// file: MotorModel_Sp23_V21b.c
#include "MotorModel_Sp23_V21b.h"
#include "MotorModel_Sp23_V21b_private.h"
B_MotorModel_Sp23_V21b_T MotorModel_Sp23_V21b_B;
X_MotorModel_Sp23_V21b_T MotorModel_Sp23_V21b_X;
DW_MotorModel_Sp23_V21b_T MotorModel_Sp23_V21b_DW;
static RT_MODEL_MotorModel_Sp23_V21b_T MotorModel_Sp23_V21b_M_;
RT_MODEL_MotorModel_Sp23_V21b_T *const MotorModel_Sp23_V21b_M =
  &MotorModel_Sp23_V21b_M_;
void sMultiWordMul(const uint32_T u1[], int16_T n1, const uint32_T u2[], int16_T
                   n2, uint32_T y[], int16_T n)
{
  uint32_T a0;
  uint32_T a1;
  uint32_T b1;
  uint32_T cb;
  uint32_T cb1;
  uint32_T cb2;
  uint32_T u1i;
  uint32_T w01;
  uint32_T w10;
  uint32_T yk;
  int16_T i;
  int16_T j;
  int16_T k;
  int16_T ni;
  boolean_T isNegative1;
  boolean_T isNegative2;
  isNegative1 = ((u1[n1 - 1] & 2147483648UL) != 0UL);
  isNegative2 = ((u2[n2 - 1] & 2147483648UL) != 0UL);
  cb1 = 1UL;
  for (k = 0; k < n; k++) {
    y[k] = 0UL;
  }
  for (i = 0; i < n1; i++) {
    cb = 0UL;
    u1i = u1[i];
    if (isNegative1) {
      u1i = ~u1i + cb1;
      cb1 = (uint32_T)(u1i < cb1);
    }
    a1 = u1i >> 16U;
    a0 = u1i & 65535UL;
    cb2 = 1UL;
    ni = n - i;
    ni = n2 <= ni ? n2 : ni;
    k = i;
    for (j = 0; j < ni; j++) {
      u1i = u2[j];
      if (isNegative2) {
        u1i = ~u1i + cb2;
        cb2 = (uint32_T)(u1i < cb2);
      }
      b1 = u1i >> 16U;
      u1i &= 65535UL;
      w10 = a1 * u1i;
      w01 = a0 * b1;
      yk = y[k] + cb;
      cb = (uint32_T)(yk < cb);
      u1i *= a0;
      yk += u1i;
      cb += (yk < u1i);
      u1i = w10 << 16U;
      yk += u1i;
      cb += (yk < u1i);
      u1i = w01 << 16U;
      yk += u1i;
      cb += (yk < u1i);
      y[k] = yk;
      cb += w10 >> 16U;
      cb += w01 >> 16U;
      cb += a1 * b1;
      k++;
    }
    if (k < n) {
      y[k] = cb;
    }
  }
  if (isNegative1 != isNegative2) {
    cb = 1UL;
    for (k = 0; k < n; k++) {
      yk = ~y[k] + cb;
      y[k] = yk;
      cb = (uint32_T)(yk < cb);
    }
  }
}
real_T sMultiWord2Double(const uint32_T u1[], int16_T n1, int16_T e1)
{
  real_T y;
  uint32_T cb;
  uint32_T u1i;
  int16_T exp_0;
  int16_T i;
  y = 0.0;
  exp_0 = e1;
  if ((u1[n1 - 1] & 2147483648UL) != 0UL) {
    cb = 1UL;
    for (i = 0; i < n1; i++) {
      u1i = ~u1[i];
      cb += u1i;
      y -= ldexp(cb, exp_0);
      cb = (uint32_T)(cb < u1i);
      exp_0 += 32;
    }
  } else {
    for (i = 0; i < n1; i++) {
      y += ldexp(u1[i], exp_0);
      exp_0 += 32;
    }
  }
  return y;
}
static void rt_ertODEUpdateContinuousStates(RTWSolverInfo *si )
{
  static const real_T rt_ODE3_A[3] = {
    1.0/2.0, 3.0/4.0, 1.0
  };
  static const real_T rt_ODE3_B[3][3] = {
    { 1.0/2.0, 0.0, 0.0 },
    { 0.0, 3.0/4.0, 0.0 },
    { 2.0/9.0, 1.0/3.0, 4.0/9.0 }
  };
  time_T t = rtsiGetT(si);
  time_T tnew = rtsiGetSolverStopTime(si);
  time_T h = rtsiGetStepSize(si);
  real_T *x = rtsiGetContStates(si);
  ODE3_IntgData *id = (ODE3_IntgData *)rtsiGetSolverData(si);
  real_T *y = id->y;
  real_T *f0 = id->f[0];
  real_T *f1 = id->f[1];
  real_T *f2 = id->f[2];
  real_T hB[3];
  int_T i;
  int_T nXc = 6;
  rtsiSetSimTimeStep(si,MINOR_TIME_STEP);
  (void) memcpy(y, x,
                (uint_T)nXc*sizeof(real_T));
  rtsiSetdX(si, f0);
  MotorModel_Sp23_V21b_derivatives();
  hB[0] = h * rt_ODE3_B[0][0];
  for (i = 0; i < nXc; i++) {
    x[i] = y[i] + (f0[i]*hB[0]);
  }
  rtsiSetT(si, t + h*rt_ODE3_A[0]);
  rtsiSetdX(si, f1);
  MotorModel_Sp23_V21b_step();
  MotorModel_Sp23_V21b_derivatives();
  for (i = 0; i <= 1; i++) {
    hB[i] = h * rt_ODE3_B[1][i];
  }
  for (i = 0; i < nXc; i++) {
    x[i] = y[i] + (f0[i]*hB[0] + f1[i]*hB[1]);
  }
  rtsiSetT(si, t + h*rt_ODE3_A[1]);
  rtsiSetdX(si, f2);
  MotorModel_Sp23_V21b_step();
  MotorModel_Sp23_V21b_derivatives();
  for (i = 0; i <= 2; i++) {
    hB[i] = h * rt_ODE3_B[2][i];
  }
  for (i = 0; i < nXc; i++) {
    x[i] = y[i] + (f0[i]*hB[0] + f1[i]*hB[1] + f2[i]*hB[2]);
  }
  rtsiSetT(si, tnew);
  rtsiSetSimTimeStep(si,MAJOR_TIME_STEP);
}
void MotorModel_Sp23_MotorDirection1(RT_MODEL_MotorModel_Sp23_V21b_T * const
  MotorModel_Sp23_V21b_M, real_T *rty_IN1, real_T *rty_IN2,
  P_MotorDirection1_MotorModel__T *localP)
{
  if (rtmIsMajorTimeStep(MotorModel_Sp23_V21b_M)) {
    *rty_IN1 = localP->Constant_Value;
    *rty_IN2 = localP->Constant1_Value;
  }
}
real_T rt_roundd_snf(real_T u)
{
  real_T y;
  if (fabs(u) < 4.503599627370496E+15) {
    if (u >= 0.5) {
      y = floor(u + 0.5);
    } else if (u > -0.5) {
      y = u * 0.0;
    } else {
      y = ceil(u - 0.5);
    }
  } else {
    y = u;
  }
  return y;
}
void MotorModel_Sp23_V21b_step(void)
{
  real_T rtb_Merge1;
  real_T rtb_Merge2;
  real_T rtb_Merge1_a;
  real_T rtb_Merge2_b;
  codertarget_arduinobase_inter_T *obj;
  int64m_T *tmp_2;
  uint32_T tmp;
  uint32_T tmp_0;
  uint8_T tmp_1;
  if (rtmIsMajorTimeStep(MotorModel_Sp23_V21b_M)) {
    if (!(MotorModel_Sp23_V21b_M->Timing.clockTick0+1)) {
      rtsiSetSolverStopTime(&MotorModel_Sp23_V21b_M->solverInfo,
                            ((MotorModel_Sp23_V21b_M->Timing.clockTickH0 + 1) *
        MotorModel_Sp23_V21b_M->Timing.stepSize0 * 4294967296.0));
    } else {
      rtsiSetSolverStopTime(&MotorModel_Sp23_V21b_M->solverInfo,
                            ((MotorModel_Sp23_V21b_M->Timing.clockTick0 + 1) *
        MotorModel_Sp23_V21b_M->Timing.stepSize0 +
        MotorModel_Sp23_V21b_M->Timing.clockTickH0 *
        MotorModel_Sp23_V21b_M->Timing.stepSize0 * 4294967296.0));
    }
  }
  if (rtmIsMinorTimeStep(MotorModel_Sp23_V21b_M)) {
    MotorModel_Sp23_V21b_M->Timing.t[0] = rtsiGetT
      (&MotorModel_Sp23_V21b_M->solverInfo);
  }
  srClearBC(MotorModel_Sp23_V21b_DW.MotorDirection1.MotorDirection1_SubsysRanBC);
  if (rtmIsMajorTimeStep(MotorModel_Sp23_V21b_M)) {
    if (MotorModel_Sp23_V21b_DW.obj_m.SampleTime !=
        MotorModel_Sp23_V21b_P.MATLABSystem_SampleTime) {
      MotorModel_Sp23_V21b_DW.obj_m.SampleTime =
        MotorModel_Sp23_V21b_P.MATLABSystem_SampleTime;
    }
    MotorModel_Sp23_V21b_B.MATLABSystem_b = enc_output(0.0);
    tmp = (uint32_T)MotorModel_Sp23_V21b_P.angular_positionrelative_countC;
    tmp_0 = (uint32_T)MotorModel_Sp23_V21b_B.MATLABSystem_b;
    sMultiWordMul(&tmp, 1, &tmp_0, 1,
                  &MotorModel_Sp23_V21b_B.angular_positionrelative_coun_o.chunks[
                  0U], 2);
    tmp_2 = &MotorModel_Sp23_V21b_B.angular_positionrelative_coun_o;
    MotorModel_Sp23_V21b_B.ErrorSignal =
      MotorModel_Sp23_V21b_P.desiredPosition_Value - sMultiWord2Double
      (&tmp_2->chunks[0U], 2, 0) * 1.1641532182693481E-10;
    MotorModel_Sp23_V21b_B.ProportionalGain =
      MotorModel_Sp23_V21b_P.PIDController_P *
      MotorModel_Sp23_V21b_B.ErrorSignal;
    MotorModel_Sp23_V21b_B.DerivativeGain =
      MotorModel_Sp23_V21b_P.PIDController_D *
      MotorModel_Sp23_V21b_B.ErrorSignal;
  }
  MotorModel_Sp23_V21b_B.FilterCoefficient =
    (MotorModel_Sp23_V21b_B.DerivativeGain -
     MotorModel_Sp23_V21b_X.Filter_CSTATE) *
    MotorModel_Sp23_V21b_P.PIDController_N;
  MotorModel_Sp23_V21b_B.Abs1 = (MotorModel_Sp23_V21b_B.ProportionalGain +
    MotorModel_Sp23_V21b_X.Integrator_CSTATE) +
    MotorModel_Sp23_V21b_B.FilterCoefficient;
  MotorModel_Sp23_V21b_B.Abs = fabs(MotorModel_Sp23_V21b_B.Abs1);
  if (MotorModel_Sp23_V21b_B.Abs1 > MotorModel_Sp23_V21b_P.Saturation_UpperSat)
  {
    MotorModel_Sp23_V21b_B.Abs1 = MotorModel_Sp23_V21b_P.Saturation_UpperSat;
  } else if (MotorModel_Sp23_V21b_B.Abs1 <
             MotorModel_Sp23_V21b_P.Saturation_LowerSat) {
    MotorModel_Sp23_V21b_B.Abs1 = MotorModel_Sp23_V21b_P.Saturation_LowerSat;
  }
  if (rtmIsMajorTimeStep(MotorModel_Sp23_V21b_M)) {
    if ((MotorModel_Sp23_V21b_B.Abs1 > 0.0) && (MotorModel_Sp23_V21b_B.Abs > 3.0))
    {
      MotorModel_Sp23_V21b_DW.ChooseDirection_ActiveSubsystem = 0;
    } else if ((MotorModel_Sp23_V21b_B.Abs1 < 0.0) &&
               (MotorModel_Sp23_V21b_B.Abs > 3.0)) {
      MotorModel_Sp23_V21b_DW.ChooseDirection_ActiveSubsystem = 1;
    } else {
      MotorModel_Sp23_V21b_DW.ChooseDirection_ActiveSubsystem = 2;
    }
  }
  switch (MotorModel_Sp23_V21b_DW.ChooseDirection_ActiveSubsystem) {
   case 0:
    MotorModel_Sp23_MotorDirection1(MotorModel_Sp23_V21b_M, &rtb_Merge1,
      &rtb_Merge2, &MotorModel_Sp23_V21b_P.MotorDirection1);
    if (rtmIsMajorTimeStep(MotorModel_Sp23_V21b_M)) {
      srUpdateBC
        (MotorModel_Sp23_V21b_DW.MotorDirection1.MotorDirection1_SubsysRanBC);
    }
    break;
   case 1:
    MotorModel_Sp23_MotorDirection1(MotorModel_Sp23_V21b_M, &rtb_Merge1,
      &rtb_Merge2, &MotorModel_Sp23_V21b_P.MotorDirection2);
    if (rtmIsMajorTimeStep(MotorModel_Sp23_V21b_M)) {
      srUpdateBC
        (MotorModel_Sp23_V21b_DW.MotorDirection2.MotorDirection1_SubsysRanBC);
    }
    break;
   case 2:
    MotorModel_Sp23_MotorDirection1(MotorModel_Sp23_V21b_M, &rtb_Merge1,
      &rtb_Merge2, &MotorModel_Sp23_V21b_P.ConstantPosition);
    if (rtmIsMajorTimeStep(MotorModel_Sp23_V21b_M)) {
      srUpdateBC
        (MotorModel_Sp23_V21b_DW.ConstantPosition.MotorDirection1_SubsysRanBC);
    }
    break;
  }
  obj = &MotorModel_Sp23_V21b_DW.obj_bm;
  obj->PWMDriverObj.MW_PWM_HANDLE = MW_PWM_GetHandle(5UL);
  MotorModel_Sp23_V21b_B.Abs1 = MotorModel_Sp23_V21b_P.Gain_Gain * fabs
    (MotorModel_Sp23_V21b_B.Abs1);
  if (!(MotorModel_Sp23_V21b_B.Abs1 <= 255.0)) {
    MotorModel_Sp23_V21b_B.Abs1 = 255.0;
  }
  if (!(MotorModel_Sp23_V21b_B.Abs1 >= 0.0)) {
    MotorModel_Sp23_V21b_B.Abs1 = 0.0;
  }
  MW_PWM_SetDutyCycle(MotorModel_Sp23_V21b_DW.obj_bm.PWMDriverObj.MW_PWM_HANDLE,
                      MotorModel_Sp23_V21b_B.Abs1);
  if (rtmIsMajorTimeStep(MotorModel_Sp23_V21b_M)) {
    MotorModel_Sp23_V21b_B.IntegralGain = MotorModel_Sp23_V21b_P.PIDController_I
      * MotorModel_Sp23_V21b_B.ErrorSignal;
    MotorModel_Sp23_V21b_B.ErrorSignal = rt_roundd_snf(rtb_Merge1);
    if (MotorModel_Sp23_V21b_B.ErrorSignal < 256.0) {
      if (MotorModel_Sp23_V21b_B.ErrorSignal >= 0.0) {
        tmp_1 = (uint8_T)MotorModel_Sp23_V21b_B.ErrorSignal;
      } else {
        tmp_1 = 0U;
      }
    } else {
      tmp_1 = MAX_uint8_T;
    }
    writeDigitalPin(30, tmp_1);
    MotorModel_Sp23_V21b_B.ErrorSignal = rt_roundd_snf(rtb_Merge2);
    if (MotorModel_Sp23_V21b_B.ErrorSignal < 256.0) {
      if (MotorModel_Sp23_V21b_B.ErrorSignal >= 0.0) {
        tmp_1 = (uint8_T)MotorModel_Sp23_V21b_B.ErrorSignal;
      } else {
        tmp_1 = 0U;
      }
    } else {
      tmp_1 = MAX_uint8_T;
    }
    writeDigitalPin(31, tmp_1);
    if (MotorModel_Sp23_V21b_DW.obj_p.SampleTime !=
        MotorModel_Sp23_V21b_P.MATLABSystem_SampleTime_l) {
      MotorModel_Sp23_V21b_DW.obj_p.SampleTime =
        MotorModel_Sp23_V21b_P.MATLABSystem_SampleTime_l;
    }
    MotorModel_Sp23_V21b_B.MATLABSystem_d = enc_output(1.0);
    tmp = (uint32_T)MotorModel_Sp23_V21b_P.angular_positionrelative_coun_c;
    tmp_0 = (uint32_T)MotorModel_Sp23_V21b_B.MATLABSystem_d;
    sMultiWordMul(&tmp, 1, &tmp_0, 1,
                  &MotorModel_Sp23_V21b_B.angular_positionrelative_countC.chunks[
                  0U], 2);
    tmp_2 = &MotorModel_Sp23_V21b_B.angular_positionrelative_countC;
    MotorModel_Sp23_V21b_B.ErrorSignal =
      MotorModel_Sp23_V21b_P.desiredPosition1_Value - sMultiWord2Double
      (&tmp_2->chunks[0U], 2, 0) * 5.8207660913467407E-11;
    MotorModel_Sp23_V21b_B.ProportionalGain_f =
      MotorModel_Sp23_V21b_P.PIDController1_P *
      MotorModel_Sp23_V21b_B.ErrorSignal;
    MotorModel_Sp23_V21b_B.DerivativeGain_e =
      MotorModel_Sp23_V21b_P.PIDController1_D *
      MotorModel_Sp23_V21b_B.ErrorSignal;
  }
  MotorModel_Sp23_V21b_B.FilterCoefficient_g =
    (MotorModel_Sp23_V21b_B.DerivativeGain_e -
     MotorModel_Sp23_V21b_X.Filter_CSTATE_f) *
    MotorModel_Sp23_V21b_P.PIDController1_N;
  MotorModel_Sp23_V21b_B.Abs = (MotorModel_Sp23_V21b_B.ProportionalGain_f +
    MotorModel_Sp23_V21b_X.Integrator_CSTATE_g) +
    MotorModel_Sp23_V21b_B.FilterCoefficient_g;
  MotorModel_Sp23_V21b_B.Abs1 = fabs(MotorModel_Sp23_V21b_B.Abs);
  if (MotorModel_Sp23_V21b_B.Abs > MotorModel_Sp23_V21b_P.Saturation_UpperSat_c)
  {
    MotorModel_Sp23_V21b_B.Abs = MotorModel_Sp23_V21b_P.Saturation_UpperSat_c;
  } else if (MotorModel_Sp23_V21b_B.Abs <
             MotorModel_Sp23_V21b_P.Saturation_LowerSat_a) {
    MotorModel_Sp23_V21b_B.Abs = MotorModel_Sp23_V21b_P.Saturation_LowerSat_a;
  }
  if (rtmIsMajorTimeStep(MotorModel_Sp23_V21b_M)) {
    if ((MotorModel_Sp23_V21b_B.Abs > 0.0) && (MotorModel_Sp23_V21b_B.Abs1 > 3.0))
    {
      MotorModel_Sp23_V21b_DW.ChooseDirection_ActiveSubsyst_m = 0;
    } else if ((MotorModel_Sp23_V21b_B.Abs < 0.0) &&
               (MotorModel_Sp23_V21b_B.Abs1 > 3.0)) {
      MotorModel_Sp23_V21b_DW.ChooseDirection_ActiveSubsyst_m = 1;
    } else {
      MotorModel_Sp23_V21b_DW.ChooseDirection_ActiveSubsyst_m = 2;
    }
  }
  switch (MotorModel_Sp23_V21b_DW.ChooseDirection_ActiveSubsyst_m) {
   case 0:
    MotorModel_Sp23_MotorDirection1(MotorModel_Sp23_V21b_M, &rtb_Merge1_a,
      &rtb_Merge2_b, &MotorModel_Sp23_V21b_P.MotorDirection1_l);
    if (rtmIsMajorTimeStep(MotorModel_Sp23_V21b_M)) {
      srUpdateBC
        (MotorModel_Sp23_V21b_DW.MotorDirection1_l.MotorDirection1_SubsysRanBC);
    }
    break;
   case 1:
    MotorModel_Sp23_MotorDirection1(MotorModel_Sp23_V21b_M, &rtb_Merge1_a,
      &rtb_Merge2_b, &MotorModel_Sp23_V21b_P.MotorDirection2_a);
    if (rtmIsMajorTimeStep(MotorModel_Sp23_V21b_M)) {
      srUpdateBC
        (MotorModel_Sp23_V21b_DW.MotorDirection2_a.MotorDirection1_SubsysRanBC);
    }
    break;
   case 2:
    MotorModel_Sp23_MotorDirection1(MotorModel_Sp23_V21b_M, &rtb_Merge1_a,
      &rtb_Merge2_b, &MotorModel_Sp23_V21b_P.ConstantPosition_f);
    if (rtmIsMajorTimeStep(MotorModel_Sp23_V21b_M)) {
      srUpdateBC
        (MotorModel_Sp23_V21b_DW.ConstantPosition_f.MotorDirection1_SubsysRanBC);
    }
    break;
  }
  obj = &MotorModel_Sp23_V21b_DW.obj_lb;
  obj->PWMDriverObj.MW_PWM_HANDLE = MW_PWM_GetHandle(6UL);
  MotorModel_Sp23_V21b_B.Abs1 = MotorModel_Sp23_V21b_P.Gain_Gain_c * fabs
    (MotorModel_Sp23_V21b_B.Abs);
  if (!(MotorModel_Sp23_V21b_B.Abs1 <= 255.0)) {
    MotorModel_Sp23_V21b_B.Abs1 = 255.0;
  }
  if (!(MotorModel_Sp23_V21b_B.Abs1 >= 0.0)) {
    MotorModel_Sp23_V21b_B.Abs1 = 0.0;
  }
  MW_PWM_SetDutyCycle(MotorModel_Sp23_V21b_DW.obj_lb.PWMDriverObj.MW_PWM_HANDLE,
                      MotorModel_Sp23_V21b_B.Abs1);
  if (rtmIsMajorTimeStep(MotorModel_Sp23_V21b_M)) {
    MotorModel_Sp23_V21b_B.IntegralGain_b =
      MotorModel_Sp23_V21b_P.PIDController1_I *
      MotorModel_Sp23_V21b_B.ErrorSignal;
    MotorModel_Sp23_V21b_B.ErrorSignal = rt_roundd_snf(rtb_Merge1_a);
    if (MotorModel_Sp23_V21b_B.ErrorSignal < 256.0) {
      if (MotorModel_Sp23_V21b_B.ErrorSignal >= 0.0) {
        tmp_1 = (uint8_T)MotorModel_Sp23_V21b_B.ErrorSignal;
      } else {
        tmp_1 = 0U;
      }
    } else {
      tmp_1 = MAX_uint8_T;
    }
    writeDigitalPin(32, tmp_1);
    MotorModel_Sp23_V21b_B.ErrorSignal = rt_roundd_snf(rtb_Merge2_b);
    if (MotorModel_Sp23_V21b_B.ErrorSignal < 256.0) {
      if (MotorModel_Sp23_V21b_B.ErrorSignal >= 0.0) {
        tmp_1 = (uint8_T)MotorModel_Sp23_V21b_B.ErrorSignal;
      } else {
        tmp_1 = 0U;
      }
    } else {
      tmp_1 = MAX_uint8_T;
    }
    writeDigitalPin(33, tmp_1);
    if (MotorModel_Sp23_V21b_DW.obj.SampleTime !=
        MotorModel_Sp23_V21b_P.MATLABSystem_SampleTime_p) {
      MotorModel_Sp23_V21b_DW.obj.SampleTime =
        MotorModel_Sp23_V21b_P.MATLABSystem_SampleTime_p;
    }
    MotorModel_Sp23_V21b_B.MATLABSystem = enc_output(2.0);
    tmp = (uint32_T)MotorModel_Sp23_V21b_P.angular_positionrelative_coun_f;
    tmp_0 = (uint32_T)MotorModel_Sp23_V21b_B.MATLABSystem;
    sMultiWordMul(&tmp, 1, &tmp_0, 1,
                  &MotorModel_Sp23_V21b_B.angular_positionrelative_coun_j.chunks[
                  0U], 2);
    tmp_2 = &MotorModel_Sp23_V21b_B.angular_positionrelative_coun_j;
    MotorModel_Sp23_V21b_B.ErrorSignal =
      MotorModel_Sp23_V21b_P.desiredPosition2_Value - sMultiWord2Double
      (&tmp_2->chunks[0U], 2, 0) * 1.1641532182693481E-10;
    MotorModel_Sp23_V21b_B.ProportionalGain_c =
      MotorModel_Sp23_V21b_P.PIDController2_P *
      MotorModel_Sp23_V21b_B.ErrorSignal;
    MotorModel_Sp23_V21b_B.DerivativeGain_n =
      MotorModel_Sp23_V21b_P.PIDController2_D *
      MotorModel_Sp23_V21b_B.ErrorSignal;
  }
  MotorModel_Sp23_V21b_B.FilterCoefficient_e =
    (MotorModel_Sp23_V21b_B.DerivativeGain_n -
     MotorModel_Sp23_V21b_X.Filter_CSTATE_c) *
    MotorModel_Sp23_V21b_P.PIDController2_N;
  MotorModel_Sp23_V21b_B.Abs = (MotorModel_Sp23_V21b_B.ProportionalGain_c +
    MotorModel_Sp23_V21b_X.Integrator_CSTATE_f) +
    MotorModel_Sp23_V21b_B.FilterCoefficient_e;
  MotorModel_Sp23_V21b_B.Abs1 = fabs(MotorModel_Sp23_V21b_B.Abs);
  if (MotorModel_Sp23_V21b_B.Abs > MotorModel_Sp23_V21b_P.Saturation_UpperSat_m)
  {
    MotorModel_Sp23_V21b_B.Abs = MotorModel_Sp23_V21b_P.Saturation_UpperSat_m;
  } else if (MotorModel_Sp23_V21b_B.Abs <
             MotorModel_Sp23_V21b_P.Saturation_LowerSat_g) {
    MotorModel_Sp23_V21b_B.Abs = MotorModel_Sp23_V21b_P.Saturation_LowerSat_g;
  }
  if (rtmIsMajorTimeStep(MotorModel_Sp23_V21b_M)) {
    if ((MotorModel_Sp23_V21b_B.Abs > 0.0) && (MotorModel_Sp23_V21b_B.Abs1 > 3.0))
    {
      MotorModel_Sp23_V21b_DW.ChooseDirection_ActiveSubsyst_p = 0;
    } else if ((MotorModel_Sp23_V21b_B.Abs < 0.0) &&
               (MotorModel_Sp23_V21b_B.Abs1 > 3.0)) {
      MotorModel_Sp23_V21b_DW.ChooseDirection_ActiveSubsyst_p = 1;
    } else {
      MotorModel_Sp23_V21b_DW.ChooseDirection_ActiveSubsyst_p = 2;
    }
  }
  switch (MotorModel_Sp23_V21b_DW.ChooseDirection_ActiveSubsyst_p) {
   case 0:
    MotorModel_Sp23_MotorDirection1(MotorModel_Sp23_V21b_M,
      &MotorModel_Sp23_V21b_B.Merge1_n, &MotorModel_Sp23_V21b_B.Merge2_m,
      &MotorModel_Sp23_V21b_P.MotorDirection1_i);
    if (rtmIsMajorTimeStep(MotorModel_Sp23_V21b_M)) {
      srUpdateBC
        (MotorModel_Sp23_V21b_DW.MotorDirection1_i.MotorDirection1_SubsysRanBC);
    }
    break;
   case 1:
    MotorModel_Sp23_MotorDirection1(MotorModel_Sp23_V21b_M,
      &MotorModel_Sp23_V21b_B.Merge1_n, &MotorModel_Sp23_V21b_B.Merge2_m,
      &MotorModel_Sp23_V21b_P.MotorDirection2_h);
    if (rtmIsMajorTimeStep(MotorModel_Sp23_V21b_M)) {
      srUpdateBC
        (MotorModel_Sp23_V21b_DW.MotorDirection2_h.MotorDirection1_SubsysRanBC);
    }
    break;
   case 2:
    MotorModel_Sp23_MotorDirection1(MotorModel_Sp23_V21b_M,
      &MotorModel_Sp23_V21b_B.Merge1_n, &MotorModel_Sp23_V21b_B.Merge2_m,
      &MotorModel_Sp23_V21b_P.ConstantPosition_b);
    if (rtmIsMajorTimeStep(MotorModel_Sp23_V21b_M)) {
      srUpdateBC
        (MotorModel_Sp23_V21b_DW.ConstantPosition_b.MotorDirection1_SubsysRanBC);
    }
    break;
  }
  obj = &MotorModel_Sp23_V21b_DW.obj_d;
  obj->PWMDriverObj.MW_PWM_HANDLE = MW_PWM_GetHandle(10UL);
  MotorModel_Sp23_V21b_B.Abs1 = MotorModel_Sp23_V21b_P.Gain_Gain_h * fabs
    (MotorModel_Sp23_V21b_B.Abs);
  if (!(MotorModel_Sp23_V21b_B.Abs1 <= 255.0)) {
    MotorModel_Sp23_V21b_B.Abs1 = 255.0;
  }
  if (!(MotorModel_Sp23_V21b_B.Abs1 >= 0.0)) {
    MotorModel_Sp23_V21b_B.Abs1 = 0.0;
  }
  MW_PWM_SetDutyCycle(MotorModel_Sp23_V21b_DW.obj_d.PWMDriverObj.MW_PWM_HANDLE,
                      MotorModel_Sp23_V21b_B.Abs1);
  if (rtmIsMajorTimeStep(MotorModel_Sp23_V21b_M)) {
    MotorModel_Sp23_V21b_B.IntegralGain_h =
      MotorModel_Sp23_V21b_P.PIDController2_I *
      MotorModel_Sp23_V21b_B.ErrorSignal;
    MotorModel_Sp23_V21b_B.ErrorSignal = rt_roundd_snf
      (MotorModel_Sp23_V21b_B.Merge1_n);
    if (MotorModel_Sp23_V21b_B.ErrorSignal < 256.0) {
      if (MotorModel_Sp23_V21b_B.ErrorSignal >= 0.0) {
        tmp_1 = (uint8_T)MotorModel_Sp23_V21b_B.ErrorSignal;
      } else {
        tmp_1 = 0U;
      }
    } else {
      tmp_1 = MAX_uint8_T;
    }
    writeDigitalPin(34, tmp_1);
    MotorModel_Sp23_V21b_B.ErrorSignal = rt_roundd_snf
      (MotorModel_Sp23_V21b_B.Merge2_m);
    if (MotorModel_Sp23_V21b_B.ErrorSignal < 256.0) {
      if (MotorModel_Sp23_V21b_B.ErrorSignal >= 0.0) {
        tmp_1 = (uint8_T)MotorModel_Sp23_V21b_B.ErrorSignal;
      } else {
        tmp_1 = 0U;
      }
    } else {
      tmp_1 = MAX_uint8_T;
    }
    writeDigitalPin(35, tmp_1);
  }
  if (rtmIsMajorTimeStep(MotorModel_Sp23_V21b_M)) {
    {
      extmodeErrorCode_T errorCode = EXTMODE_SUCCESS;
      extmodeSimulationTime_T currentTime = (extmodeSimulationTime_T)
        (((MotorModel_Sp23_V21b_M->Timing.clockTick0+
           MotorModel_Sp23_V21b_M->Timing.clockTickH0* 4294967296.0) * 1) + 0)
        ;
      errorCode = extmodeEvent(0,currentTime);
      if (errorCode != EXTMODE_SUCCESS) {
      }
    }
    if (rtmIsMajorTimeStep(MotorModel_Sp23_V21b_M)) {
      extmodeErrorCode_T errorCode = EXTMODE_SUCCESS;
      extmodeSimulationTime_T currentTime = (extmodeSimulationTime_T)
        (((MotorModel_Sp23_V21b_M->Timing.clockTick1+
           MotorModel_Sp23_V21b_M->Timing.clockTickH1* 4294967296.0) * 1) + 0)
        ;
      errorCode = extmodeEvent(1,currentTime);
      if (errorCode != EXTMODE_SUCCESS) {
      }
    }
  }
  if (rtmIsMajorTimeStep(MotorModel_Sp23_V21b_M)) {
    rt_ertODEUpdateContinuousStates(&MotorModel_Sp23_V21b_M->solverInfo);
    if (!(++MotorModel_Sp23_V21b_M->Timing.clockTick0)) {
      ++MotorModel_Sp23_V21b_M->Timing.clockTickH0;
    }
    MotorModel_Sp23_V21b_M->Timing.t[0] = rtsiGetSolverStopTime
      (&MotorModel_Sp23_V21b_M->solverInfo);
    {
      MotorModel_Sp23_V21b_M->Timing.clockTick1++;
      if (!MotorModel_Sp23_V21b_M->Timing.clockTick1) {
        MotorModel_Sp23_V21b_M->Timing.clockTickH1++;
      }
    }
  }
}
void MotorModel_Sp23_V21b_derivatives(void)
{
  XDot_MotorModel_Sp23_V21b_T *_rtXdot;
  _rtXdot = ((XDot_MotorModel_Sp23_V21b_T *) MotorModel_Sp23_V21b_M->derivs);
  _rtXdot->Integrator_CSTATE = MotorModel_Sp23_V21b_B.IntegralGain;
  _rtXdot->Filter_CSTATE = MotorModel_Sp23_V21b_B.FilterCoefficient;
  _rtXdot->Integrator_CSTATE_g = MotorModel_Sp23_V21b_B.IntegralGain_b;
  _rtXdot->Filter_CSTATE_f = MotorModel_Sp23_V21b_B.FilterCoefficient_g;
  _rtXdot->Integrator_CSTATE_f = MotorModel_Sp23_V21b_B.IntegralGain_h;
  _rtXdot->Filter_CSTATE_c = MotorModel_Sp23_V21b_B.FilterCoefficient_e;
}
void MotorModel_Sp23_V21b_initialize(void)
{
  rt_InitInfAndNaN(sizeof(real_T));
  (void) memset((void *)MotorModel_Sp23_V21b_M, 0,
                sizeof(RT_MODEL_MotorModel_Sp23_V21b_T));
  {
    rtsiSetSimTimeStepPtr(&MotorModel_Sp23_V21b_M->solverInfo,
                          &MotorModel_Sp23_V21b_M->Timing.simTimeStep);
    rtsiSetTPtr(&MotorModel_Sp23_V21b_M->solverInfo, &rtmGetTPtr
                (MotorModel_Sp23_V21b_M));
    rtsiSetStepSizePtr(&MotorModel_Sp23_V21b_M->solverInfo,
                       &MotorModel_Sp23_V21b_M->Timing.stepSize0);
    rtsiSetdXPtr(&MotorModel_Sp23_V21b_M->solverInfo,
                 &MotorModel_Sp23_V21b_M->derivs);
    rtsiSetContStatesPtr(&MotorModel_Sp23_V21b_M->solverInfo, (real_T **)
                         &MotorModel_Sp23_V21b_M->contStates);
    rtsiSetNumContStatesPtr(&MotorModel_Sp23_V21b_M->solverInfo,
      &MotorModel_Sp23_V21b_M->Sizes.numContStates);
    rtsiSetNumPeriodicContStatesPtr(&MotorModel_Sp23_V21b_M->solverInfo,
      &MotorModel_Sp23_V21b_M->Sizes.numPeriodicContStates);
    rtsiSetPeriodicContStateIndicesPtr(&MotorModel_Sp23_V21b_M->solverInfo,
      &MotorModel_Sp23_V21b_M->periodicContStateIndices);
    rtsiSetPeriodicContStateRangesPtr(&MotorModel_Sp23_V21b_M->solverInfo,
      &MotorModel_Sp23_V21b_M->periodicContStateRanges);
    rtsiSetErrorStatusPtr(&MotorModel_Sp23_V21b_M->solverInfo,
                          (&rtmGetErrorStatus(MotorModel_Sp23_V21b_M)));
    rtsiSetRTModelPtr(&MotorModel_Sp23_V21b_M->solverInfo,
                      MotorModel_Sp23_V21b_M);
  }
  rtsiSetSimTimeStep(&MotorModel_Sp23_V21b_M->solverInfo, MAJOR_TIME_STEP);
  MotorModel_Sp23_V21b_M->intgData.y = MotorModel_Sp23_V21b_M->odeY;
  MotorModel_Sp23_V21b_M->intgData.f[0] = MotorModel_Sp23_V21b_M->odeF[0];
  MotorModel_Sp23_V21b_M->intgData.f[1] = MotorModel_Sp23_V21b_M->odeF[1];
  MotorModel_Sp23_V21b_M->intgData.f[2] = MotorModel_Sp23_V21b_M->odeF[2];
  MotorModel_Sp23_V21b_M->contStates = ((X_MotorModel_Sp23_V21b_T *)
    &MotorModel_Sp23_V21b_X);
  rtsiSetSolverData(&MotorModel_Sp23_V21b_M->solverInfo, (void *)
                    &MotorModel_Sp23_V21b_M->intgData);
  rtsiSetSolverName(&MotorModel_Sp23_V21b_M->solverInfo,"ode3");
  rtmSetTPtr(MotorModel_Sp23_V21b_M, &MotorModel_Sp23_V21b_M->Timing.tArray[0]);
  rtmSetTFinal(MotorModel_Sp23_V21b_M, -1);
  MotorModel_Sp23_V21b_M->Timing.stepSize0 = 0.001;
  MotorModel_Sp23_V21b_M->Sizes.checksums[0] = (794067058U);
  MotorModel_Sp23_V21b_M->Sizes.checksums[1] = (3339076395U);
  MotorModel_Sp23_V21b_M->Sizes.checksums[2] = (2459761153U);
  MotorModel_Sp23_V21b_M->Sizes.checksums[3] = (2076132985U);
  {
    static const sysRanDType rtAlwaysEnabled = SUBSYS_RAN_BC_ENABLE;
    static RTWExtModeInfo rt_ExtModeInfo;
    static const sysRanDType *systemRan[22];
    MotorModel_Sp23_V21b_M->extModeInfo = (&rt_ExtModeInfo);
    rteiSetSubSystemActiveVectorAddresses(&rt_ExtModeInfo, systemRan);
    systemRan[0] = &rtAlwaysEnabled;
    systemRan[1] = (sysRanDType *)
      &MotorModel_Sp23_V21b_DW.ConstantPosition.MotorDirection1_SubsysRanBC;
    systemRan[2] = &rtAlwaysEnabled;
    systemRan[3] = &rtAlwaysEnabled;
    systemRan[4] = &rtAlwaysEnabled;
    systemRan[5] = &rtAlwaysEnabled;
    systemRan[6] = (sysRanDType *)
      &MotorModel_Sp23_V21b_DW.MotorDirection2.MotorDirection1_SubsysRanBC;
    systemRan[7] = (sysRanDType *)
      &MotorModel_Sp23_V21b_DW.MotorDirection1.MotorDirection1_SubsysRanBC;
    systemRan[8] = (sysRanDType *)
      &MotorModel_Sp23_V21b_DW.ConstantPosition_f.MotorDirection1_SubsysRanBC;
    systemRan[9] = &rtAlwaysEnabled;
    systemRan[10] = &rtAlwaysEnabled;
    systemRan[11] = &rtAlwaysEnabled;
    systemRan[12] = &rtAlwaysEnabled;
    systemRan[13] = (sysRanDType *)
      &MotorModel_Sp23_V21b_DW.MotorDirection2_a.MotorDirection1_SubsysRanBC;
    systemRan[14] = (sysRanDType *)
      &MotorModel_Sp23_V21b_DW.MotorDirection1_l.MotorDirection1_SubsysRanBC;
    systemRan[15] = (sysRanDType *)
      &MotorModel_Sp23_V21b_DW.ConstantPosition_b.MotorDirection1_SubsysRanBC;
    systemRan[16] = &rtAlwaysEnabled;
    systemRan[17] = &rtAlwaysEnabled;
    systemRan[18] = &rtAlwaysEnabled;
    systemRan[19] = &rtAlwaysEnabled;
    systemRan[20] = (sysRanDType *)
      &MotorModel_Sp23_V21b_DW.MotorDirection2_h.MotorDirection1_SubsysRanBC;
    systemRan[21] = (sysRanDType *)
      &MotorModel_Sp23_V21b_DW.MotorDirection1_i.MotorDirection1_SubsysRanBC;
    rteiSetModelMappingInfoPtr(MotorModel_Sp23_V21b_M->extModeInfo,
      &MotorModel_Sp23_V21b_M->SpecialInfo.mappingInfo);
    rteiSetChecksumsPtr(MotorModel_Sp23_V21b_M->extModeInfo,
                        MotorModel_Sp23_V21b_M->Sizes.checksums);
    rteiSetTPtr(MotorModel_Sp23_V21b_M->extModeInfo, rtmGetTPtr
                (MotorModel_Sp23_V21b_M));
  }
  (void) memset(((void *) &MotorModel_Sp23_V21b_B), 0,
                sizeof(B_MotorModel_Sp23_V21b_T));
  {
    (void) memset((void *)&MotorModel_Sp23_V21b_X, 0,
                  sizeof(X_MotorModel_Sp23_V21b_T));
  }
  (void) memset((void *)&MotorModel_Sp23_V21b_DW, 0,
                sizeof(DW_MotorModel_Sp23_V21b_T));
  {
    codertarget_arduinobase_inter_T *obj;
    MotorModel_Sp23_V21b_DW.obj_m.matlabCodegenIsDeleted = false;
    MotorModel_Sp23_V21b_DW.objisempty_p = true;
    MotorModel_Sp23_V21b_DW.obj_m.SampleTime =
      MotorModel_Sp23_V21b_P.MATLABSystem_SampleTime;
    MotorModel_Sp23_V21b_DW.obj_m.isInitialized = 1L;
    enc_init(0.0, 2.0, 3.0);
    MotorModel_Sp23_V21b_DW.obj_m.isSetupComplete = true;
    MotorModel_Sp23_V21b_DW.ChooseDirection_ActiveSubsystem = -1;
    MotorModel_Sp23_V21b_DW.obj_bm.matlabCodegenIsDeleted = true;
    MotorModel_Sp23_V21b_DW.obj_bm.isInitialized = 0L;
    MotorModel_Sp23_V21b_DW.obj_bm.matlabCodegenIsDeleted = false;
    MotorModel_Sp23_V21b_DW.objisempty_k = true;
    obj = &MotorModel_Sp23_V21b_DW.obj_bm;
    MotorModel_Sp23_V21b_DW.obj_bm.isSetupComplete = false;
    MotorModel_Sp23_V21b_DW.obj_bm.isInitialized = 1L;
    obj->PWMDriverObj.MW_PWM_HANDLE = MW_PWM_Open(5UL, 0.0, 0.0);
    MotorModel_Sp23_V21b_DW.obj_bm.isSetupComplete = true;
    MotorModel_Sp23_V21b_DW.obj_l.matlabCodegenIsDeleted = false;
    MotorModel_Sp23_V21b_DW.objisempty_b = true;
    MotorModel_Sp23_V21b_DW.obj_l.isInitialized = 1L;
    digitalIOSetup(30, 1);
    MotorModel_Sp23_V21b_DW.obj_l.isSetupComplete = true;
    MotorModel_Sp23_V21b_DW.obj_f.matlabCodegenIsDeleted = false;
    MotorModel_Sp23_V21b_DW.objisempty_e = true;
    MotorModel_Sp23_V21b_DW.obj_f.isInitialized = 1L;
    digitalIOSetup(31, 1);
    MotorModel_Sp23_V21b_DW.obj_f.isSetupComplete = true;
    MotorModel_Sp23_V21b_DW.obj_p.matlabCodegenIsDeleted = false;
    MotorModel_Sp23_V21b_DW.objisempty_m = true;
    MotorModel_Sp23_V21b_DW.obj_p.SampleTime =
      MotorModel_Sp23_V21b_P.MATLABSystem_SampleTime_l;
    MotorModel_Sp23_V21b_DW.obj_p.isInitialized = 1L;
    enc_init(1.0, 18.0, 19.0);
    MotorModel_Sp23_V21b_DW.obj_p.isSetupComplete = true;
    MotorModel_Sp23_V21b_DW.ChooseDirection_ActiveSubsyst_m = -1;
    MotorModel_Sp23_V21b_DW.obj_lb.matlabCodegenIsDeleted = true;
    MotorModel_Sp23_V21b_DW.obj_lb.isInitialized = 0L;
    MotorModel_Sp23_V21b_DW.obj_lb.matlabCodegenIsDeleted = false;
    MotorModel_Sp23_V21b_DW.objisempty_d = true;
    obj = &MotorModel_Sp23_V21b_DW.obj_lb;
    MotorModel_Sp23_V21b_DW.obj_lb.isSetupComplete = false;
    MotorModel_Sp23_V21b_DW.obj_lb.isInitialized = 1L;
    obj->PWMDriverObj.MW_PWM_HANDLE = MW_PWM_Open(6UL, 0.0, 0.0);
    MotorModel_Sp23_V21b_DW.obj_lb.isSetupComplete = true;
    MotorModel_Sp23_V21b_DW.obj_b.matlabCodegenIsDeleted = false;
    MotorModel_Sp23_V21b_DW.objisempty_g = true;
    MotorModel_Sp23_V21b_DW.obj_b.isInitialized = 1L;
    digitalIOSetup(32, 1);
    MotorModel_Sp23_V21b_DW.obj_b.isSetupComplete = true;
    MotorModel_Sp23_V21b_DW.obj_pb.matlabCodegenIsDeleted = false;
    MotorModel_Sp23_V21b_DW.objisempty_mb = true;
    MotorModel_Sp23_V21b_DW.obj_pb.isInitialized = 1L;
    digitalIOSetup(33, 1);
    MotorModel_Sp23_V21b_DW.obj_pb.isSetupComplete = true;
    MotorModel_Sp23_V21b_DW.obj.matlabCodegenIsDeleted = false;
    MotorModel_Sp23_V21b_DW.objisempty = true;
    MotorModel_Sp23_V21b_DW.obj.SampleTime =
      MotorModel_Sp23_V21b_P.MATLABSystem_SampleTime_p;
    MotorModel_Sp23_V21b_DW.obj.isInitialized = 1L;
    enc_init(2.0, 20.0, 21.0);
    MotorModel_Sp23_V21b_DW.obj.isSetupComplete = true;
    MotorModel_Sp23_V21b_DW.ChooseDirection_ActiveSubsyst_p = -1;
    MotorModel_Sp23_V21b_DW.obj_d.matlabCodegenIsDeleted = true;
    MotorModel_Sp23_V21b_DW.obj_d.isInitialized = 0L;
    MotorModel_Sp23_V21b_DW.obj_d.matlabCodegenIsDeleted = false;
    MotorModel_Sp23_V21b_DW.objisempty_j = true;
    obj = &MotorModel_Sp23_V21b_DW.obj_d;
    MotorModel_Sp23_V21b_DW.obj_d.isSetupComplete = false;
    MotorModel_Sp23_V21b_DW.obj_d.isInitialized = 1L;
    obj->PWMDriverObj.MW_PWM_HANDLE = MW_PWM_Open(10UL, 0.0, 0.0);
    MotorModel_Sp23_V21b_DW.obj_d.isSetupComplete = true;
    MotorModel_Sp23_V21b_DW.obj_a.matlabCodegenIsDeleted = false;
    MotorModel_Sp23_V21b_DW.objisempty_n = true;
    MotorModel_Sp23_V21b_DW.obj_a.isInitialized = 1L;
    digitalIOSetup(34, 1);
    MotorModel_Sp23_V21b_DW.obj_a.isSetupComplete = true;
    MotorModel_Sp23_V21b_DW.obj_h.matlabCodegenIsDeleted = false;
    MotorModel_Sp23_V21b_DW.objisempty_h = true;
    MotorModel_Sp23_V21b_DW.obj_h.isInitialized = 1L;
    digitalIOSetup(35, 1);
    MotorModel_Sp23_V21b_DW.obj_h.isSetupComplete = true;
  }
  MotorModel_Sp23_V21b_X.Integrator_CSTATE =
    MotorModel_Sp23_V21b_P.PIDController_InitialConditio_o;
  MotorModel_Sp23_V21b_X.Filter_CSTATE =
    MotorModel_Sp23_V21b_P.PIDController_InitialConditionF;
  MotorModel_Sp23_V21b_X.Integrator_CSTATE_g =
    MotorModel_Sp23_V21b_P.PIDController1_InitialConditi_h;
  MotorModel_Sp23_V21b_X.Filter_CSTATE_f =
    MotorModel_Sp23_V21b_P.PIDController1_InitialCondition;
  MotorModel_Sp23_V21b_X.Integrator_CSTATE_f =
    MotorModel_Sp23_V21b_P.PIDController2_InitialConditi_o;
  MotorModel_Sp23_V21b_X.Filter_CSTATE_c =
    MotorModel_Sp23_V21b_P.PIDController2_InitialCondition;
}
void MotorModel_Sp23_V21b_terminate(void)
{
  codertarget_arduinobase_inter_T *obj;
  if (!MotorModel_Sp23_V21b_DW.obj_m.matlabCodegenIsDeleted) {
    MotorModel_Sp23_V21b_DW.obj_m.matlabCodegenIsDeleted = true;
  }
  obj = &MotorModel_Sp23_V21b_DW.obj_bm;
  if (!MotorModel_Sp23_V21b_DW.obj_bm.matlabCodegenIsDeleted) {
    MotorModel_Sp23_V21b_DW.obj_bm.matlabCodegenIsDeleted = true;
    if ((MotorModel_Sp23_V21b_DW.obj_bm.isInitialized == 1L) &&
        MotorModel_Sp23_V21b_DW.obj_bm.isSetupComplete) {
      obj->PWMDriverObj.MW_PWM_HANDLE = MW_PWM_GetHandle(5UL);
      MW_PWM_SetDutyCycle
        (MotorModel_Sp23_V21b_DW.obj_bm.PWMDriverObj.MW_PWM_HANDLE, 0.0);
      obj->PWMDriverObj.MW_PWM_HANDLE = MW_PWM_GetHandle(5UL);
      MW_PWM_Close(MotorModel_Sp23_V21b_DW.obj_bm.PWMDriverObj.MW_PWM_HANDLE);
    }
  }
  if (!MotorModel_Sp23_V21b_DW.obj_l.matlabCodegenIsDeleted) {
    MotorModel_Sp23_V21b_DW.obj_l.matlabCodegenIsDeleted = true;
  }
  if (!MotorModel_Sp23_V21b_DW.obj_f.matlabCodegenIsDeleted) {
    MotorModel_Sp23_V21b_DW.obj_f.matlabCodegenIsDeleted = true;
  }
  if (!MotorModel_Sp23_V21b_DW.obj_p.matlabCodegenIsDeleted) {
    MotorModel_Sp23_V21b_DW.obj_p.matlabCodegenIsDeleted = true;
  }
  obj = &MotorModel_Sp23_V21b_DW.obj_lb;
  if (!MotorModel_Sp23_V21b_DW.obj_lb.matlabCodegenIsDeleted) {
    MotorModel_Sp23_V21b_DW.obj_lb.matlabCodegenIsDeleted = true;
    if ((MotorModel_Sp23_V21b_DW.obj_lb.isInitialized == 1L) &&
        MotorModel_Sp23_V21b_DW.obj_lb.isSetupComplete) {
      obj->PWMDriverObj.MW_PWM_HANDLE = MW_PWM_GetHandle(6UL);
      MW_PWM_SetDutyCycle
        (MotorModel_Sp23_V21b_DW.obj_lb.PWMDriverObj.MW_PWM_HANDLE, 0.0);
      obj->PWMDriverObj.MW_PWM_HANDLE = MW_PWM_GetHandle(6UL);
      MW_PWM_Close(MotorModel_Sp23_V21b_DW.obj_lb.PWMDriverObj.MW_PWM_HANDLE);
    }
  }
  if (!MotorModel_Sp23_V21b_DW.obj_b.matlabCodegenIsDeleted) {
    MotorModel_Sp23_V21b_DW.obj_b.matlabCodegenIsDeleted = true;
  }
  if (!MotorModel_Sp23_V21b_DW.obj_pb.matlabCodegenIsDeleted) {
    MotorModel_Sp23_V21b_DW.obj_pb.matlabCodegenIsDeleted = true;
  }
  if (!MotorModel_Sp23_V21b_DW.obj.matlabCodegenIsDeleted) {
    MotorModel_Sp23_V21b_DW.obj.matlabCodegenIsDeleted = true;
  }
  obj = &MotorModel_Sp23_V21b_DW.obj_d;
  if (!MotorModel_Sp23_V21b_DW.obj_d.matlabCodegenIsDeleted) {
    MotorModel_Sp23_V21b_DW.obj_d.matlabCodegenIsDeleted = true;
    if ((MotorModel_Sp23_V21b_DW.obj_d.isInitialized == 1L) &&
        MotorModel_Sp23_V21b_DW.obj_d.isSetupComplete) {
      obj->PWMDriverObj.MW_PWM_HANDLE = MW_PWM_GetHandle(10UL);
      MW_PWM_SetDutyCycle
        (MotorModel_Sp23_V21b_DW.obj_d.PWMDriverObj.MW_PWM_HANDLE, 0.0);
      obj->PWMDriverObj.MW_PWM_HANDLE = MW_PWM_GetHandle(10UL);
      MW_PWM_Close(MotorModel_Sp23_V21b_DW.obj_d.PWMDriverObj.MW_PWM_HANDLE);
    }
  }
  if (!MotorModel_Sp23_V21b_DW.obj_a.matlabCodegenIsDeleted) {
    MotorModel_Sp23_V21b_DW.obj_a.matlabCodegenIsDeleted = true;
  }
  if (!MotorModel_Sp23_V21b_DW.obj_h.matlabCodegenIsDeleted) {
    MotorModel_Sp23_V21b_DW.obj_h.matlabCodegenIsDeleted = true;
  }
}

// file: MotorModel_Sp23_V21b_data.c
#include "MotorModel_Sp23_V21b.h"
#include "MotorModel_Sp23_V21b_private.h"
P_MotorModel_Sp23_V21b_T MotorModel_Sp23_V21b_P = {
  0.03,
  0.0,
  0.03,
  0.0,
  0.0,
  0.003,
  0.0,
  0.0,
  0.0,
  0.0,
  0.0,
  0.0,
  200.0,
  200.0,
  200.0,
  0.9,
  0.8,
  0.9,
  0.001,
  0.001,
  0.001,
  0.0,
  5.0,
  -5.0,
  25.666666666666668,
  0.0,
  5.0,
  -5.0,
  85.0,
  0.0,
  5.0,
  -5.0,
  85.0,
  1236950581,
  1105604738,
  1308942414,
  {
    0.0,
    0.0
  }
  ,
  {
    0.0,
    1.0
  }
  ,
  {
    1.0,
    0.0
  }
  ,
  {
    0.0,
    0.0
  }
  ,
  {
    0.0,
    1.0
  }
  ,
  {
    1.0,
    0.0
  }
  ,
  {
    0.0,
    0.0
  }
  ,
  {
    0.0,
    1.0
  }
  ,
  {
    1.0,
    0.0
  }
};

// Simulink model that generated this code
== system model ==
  PWM#1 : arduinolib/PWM  pinNumber=5  <- 1: Gain
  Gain : Gain  Gain=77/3  <- 1: Abs
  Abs : Abs  <- 1: Saturation
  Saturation : Saturate  UpperLimit=5  LowerLimit=-5  <- 1: PIDController
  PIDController : slpidlib/PID Controller  Controller=PID  Form=Parallel  TimeDomain=Continuous-time  IntegratorMethod=Forward Euler  P=0.9  I=0  D=0.03  N=200  InitialConditionForIntegrator=0  ExternalReset=none  LimitOutput=off  UpperSaturationLimit=inf  LowerSaturationLimit=-inf  <- 1: Sum#1
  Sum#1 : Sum  Inputs=+-  <- 1: desiredPosition, 2: Gain#1
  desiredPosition : Constant  Value=0
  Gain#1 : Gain  Gain=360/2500  <- 1: MATLABSystem
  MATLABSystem : MATLABSystem
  PWM#2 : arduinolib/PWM  pinNumber=6  <- 1: Gain#2
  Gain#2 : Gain  Gain=255/3  <- 1: Abs#1
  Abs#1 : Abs  <- 1: Saturate#1
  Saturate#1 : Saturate  UpperLimit=5  LowerLimit=-5  <- 1: PIDController1
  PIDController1 : slpidlib/PID Controller  Controller=PID  Form=Parallel  TimeDomain=Continuous-time  IntegratorMethod=Forward Euler  P=0.8  I=0  D=0  N=200  InitialConditionForIntegrator=0  ExternalReset=none  LimitOutput=off  UpperSaturationLimit=inf  LowerSaturationLimit=-inf  <- 1: Sum#2
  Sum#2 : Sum  Inputs=+-  <- 1: desiredPosition1, 2: Gain#3
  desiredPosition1 : Constant  Value=0
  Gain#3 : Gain  Gain=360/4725  <- 1: MATLABSystem#1
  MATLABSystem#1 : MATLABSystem
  PWM#3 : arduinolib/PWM  pinNumber=10  <- 1: Gain#4
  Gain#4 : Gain  Gain=255/3  <- 1: Abs#2
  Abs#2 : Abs  <- 1: Saturate#2
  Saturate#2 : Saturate  UpperLimit=5  LowerLimit=-5  <- 1: PIDController2
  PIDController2 : slpidlib/PID Controller  Controller=PID  Form=Parallel  TimeDomain=Continuous-time  IntegratorMethod=Forward Euler  P=0.9  I=0.003  D=0.03  N=200  InitialConditionForIntegrator=0  ExternalReset=none  LimitOutput=off  UpperSaturationLimit=inf  LowerSaturationLimit=-inf  <- 1: Sum#3
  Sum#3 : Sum  Inputs=+-  <- 1: desiredPosition2, 2: Gain#5
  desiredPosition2 : Constant  Value=0
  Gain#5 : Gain  Gain=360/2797  <- 1: MATLABSystem#2
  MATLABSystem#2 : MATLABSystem
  DigitalOutput#1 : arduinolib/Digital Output  pinNumber=30  <- 1: Merge1
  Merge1 : Merge  Inputs=3  <- 1: MotorDirection1, 2: MotorDirection2, 3: ConstantPosition
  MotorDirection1 : Subsystem  <- Action: ChooseDirection
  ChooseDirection : If  IfExpression=u1 > 0 & u2 > 3  ElseIfExpressions=u1 < 0 & u2 > 3  <- 1: Saturation, 2: Abs1
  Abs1 : Abs  <- 1: PIDController
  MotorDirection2 : Subsystem  <- Action: ChooseDirection/2
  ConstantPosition : Subsystem  <- Action: ChooseDirection/3
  DigitalOutput#2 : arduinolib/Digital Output  pinNumber=32  <- 1: Merge#1
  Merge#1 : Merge  Inputs=3  <- 1: Subsystem#1, 2: Subsystem#2, 3: Subsystem#3
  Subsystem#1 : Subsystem  <- Action: If#1
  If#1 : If  IfExpression=u1 > 0 & u2 > 3  ElseIfExpressions=u1 < 0 & u2 > 3  <- 1: Saturate#1, 2: Abs#3
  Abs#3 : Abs  <- 1: PIDController1
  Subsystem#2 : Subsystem  <- Action: If#1/2
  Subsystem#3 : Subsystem  <- Action: If#1/3
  DigitalOutput#3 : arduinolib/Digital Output  pinNumber=34  <- 1: Merge#2
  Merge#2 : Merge  Inputs=3  <- 1: Subsystem#4, 2: Subsystem#5, 3: Subsystem#6
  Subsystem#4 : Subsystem  <- Action: If#2
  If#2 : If  IfExpression=u1 > 0 & u2 > 3  ElseIfExpressions=u1 < 0 & u2 > 3  <- 1: Saturate#2, 2: Abs#4
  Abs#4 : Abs  <- 1: PIDController2
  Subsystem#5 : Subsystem  <- Action: If#2/2
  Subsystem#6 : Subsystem  <- Action: If#2/3
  DigitalOutput#4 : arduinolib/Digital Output  pinNumber=31  <- 1: Merge2
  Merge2 : Merge  Inputs=3  <- 1: MotorDirection1/2, 2: MotorDirection2/2, 3: ConstantPosition/2
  DigitalOutput#5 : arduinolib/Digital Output  pinNumber=33  <- 1: Merge#3
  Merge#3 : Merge  Inputs=3  <- 1: Subsystem#1/2, 2: Subsystem#2/2, 3: Subsystem#3/2
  DigitalOutput#6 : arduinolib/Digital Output  pinNumber=35  <- 1: Merge#4
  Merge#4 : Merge  Inputs=3  <- 1: Subsystem#4/2, 2: Subsystem#5/2, 3: Subsystem#6/2
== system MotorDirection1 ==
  ActionPort#1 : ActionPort
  IN1 : Outport  <- 1: Constant
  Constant : Constant
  IN2 : Outport  <- 1: Constant1
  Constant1 : Constant  Value=0
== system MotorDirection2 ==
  ActionPort#2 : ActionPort
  Outport#1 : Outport  <- 1: Constant#1
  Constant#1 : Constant  Value=0
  Outport#2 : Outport  <- 1: Constant#2
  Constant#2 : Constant
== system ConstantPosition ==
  ActionPort#3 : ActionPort
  Outport#3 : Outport  <- 1: Constant#3
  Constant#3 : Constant  Value=0
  Outport#4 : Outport  <- 1: Constant#4
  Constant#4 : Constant  Value=0
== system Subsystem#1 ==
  ActionPort#4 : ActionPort
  Outport#5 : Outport  <- 1: Constant#5
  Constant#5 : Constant
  Outport#6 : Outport  <- 1: Constant#6
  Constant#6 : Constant  Value=0
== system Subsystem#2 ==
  ActionPort#5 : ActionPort
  Outport#7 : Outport  <- 1: Constant#7
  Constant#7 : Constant  Value=0
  Outport#8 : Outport  <- 1: Constant#8
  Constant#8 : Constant
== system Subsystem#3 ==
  ActionPort#6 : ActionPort
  Outport#9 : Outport  <- 1: Constant#9
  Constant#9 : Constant  Value=0
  Outport#10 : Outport  <- 1: Constant#10
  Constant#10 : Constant  Value=0
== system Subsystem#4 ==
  ActionPort#7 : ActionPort
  Outport#11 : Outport  <- 1: Constant#11
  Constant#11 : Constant
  Outport#12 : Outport  <- 1: Constant#12
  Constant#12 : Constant  Value=0
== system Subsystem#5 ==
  ActionPort#8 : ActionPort
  Outport#13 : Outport  <- 1: Constant#13
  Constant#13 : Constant  Value=0
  Outport#14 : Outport  <- 1: Constant#14
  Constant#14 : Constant
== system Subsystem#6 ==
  ActionPort#9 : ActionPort
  Outport#15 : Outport  <- 1: Constant#15
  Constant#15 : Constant  Value=0
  Outport#16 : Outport  <- 1: Constant#16
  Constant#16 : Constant  Value=0
